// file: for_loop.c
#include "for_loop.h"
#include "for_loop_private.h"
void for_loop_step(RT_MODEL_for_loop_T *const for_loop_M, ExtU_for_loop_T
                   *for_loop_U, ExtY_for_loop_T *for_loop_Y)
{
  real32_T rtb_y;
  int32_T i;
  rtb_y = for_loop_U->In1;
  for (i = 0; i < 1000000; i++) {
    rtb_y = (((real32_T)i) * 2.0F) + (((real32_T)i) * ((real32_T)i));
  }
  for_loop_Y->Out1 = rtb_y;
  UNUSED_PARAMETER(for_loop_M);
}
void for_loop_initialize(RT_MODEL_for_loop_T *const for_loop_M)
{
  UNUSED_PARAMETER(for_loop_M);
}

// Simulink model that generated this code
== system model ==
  In1 : Inport
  Out1 : Outport  <- 1: MATLABFunction#1
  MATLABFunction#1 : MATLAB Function  <- 1: In1
== matlab function MATLABFunction#1 ==
function y = fcn(u)
y = u;
for i = single(0:1000000-1)
    y = i*2+i^2;
end
